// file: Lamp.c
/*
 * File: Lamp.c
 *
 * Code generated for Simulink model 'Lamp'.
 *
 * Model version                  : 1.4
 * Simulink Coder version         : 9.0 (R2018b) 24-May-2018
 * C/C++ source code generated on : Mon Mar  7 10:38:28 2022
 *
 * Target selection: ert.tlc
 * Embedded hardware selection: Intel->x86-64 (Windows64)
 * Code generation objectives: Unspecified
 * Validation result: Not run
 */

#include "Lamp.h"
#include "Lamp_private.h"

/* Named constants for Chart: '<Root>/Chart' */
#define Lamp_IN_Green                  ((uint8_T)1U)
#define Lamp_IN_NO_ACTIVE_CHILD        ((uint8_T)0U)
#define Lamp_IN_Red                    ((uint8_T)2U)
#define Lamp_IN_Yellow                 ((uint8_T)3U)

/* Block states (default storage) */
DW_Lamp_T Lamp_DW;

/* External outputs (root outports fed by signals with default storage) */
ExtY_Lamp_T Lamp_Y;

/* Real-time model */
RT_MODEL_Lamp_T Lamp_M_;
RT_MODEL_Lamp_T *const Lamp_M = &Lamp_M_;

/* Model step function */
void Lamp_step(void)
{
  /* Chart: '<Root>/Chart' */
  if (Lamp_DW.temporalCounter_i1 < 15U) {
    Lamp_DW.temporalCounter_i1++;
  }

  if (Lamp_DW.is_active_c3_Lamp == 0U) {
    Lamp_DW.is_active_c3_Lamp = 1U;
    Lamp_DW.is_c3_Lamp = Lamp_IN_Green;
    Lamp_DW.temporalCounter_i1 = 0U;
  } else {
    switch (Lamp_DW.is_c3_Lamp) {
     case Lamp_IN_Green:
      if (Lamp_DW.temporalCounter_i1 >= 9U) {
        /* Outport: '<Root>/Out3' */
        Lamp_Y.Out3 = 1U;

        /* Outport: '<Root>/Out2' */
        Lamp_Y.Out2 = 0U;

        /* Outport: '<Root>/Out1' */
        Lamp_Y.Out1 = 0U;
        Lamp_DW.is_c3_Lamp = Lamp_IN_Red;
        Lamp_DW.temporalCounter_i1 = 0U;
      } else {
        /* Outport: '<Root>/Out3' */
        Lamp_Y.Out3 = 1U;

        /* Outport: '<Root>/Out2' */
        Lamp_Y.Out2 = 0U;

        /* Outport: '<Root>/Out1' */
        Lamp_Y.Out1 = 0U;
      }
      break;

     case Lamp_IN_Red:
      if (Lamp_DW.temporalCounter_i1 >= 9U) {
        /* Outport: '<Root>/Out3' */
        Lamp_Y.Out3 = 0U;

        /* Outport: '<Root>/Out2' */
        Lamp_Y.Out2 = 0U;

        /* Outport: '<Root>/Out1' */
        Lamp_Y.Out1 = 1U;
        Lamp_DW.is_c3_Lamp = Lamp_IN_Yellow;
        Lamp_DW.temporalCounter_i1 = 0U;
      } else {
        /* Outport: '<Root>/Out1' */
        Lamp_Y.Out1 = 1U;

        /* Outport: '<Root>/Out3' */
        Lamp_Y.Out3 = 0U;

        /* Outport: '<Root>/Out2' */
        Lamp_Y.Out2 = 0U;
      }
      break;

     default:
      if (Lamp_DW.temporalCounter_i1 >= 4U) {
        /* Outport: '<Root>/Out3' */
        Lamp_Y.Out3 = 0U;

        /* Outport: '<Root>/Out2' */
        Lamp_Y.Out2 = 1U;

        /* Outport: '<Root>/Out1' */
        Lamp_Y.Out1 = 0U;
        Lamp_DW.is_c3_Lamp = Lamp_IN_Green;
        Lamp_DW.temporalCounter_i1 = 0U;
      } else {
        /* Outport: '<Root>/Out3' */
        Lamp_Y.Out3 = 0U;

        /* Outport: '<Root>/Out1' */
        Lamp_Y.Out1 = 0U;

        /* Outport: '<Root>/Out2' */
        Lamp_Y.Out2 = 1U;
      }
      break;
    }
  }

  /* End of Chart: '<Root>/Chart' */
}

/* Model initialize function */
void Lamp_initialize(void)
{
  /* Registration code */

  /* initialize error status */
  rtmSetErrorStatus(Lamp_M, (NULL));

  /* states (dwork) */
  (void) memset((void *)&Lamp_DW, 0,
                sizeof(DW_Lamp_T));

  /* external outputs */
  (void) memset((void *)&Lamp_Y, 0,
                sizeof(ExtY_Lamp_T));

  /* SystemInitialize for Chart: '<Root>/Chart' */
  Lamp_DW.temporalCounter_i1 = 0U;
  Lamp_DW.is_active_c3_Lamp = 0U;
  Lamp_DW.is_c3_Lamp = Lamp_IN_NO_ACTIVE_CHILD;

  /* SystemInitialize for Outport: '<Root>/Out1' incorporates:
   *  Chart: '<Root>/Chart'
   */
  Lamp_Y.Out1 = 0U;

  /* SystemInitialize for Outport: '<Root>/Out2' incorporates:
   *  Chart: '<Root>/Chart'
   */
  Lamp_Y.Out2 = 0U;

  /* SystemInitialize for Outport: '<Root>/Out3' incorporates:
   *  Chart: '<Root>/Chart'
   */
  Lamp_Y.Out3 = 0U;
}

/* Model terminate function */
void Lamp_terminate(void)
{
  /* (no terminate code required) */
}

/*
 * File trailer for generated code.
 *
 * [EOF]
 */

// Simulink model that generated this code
simulink model "Lamp"  (R2018b)
settings: Solver=FixedStepDiscrete  StartTime=0.0  StopTime=30  RelTol=1e-3

== system Lamp ==
  Chart : Stateflow chart  TreatAsAtomicUnit=on
  Lamp : LampBlock  WebBlockId=9
  Lamp1 : LampBlock  WebBlockId=10
  Lamp2 : LampBlock  WebBlockId=11
  Out1 : Outport
  Out2 : Outport  Port=2
  Out3 : Outport  Port=3
  wires:
  Chart/1(red) -> Out1/1
  Chart/2(yellow) -> Out2/1
  Chart/3(green) -> Out3/1

== stateflow chart Lamp/Chart ==
  state Yellow
    en:
    du:
    green = uint8(0);
    red = uint8(0);
    yellow =uint8(1);
    ex:
  state Green
    en:
    du:
    green =uint8(1);
    yellow = uint8(0);
    red = uint8(0);
    ex:
  state Red
    en:
    du:
    red = uint8(1);
    green = uint8(0);
    yellow = uint8(0);
    ex:
  Yellow -> Green : [after(2000,msec)]{green = uint8(0);
      | yellow = uint8(1);
      | red = uint8(0);}
  (default) -> Green
  Green -> Red : [after(5000,msec)]{green = uint8(1);
      | yellow = uint8(0);
      | red = uint8(0);
      | }
  Red -> Yellow : [after(5000,msec)]{green = uint8(0);
      | yellow = uint8(0);
      | red = uint8(1);}
  data: red output uint8; yellow output uint8; green output uint8
